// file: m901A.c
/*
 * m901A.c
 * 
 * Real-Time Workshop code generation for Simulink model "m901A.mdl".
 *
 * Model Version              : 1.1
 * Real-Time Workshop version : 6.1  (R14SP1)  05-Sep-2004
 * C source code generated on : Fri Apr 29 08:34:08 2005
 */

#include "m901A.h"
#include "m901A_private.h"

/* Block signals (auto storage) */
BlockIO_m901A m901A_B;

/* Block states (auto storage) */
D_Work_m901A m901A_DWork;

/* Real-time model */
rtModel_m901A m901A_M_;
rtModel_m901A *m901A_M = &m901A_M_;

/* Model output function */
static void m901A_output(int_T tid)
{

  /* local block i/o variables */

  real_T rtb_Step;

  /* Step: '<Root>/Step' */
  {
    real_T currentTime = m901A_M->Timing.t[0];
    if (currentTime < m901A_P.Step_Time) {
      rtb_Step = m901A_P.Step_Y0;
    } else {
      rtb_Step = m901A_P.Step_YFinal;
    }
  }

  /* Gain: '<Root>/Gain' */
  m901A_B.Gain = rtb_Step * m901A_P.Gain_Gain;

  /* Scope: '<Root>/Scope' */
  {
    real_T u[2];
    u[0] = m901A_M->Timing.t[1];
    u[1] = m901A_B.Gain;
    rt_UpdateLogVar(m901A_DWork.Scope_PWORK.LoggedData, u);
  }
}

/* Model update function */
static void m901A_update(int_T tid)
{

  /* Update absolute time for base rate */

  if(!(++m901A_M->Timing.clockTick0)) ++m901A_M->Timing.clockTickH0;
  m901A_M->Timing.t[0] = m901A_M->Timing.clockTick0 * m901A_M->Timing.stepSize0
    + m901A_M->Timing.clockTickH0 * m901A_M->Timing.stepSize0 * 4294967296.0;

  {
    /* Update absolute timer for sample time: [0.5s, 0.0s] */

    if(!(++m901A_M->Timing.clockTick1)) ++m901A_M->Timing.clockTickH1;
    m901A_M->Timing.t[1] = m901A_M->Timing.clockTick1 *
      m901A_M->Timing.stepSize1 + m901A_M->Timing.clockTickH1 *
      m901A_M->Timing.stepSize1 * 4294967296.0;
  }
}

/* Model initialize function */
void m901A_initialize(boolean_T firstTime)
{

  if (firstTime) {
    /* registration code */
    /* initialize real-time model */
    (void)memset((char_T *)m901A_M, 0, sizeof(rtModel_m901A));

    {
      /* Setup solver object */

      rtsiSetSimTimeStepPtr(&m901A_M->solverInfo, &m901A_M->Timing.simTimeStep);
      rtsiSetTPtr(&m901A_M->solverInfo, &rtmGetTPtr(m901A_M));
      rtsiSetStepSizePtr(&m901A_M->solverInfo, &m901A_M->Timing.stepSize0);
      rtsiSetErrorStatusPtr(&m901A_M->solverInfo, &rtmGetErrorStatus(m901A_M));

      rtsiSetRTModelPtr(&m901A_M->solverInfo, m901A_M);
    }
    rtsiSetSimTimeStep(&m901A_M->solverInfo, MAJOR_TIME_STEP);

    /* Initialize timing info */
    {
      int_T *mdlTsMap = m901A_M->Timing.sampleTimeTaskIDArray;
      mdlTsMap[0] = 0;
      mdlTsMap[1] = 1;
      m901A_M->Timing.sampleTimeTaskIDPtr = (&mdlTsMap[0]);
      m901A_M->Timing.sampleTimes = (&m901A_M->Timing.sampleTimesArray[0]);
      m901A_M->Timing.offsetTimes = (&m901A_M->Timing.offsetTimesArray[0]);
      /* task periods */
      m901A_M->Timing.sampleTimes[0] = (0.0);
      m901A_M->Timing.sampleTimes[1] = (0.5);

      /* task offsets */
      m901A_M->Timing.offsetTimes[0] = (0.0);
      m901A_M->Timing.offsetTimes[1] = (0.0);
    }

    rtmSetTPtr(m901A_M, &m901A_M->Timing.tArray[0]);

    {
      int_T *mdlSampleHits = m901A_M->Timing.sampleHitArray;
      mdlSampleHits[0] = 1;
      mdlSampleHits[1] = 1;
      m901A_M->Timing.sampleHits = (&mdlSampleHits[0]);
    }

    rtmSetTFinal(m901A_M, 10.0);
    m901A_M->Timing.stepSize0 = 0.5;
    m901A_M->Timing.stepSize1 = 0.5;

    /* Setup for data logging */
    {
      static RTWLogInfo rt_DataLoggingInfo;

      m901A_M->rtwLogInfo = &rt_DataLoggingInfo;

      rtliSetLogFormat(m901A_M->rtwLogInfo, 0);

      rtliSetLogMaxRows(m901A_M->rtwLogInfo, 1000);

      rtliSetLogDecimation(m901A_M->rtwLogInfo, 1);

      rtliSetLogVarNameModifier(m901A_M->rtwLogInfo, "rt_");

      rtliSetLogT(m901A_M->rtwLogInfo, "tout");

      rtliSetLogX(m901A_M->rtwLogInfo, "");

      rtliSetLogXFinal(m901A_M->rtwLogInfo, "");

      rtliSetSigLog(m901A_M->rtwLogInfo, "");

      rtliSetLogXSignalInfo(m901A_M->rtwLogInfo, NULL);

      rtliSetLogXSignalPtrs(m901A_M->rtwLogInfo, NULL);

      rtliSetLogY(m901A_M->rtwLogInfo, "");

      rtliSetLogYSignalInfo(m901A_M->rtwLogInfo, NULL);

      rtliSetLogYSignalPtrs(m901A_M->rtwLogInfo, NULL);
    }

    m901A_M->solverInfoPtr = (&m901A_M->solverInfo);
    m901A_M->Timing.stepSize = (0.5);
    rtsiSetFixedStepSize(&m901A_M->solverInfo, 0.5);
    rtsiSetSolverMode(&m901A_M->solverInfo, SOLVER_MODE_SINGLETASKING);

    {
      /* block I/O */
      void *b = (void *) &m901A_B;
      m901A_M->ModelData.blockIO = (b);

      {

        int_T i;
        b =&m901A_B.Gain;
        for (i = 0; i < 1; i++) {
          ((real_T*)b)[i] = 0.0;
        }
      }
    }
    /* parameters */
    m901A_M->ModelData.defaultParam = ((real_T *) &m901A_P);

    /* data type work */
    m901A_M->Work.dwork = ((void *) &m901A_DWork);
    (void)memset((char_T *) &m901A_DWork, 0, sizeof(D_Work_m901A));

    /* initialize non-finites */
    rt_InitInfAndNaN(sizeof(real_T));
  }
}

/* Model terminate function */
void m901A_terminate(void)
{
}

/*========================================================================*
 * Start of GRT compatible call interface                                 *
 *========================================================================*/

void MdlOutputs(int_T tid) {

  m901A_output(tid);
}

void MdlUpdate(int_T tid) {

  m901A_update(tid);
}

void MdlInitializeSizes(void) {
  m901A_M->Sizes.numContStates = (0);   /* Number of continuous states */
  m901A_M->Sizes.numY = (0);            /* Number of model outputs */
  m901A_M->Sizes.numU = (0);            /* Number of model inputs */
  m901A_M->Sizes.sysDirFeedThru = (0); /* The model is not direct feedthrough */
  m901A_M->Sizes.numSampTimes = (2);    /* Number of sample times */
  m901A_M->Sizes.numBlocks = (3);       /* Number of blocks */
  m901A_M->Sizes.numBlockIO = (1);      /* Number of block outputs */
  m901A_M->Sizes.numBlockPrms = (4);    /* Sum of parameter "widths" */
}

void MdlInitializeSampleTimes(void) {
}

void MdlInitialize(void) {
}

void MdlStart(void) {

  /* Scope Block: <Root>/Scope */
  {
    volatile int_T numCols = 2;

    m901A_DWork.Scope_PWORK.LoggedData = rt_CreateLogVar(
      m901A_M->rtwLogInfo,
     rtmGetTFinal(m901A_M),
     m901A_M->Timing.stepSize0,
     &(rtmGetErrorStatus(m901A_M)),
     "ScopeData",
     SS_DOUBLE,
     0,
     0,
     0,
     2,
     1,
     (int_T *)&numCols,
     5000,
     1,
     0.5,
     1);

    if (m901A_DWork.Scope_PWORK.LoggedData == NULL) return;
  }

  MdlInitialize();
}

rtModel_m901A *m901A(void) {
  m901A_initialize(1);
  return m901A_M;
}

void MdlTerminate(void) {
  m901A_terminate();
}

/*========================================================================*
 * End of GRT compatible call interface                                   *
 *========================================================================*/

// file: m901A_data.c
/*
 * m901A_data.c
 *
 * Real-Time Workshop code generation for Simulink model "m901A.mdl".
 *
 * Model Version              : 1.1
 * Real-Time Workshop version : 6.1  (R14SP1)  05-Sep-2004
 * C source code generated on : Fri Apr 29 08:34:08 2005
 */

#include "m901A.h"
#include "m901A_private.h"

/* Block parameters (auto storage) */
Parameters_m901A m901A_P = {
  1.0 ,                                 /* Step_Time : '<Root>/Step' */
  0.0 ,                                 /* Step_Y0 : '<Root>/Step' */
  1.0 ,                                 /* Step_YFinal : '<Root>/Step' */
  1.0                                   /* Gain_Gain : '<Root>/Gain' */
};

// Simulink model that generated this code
simulink model "m901A"  (Simulink 6.1)
settings: Solver=FixedStepDiscrete  StartTime=0.0  StopTime=10.0  FixedStep=0.5  RelTol=1e-3

== system m901A ==
  Gain : Gain
  Scope : Scope
  Step : Step  SampleTime=0
  wires:
  Step/1 -> Gain/1
  Gain/1 -> Scope/1
